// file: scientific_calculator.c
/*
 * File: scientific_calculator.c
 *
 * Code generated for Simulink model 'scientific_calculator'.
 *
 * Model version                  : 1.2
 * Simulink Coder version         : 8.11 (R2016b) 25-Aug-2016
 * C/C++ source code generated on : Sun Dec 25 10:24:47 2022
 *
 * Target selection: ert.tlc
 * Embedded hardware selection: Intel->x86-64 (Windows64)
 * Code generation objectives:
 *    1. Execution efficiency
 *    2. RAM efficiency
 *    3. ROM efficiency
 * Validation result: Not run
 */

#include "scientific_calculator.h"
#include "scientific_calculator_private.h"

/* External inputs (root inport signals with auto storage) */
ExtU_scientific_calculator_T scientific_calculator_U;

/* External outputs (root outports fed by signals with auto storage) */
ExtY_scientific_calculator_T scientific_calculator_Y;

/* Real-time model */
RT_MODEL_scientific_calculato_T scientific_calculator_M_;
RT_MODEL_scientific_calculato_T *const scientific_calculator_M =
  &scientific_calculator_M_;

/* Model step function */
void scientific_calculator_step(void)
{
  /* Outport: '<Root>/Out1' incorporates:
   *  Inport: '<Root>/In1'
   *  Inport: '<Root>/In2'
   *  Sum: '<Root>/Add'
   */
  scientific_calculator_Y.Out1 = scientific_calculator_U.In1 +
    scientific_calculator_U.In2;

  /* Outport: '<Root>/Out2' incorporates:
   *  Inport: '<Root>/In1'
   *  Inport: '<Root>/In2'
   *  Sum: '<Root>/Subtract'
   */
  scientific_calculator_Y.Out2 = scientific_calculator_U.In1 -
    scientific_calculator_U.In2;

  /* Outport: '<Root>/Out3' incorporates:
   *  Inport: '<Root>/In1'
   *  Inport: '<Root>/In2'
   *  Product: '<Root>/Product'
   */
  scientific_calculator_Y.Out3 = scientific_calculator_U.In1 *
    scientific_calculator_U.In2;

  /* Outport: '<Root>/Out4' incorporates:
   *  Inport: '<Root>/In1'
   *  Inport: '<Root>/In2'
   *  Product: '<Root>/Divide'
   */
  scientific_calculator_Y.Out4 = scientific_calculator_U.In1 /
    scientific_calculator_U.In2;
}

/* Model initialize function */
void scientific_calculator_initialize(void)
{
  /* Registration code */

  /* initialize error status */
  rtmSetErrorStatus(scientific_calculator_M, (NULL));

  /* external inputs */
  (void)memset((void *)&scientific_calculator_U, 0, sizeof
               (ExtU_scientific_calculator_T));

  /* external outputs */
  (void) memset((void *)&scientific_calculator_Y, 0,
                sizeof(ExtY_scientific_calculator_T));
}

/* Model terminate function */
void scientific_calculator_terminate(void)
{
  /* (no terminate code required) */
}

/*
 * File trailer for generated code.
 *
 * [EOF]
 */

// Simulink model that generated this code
simulink model "scientific_calculator"  (R2016b)
settings: Solver=FixedStepDiscrete  StartTime=0.0  StopTime=10.0  RelTol=1e-3

== system scientific_calculator ==
  In1 : Inport
  In2 : Inport  Port=2
  Add : Sum
  Divide : Product  Inputs=*/
  Product : Product
  Subtract : Sum  Inputs=+-
  Out1 : Outport
  Out2 : Outport  Port=2
  Out3 : Outport  Port=3
  Out4 : Outport  Port=4
  wires:
  Add/1 -> Out1/1
  Subtract/1 -> Out2/1
  Product/1 -> Out3/1
  Divide/1 -> Out4/1
  In1/1 -> Divide/1, Product/1, Subtract/1, Add/1
  In2/1 -> Add/2, Subtract/2, Product/2, Divide/2
